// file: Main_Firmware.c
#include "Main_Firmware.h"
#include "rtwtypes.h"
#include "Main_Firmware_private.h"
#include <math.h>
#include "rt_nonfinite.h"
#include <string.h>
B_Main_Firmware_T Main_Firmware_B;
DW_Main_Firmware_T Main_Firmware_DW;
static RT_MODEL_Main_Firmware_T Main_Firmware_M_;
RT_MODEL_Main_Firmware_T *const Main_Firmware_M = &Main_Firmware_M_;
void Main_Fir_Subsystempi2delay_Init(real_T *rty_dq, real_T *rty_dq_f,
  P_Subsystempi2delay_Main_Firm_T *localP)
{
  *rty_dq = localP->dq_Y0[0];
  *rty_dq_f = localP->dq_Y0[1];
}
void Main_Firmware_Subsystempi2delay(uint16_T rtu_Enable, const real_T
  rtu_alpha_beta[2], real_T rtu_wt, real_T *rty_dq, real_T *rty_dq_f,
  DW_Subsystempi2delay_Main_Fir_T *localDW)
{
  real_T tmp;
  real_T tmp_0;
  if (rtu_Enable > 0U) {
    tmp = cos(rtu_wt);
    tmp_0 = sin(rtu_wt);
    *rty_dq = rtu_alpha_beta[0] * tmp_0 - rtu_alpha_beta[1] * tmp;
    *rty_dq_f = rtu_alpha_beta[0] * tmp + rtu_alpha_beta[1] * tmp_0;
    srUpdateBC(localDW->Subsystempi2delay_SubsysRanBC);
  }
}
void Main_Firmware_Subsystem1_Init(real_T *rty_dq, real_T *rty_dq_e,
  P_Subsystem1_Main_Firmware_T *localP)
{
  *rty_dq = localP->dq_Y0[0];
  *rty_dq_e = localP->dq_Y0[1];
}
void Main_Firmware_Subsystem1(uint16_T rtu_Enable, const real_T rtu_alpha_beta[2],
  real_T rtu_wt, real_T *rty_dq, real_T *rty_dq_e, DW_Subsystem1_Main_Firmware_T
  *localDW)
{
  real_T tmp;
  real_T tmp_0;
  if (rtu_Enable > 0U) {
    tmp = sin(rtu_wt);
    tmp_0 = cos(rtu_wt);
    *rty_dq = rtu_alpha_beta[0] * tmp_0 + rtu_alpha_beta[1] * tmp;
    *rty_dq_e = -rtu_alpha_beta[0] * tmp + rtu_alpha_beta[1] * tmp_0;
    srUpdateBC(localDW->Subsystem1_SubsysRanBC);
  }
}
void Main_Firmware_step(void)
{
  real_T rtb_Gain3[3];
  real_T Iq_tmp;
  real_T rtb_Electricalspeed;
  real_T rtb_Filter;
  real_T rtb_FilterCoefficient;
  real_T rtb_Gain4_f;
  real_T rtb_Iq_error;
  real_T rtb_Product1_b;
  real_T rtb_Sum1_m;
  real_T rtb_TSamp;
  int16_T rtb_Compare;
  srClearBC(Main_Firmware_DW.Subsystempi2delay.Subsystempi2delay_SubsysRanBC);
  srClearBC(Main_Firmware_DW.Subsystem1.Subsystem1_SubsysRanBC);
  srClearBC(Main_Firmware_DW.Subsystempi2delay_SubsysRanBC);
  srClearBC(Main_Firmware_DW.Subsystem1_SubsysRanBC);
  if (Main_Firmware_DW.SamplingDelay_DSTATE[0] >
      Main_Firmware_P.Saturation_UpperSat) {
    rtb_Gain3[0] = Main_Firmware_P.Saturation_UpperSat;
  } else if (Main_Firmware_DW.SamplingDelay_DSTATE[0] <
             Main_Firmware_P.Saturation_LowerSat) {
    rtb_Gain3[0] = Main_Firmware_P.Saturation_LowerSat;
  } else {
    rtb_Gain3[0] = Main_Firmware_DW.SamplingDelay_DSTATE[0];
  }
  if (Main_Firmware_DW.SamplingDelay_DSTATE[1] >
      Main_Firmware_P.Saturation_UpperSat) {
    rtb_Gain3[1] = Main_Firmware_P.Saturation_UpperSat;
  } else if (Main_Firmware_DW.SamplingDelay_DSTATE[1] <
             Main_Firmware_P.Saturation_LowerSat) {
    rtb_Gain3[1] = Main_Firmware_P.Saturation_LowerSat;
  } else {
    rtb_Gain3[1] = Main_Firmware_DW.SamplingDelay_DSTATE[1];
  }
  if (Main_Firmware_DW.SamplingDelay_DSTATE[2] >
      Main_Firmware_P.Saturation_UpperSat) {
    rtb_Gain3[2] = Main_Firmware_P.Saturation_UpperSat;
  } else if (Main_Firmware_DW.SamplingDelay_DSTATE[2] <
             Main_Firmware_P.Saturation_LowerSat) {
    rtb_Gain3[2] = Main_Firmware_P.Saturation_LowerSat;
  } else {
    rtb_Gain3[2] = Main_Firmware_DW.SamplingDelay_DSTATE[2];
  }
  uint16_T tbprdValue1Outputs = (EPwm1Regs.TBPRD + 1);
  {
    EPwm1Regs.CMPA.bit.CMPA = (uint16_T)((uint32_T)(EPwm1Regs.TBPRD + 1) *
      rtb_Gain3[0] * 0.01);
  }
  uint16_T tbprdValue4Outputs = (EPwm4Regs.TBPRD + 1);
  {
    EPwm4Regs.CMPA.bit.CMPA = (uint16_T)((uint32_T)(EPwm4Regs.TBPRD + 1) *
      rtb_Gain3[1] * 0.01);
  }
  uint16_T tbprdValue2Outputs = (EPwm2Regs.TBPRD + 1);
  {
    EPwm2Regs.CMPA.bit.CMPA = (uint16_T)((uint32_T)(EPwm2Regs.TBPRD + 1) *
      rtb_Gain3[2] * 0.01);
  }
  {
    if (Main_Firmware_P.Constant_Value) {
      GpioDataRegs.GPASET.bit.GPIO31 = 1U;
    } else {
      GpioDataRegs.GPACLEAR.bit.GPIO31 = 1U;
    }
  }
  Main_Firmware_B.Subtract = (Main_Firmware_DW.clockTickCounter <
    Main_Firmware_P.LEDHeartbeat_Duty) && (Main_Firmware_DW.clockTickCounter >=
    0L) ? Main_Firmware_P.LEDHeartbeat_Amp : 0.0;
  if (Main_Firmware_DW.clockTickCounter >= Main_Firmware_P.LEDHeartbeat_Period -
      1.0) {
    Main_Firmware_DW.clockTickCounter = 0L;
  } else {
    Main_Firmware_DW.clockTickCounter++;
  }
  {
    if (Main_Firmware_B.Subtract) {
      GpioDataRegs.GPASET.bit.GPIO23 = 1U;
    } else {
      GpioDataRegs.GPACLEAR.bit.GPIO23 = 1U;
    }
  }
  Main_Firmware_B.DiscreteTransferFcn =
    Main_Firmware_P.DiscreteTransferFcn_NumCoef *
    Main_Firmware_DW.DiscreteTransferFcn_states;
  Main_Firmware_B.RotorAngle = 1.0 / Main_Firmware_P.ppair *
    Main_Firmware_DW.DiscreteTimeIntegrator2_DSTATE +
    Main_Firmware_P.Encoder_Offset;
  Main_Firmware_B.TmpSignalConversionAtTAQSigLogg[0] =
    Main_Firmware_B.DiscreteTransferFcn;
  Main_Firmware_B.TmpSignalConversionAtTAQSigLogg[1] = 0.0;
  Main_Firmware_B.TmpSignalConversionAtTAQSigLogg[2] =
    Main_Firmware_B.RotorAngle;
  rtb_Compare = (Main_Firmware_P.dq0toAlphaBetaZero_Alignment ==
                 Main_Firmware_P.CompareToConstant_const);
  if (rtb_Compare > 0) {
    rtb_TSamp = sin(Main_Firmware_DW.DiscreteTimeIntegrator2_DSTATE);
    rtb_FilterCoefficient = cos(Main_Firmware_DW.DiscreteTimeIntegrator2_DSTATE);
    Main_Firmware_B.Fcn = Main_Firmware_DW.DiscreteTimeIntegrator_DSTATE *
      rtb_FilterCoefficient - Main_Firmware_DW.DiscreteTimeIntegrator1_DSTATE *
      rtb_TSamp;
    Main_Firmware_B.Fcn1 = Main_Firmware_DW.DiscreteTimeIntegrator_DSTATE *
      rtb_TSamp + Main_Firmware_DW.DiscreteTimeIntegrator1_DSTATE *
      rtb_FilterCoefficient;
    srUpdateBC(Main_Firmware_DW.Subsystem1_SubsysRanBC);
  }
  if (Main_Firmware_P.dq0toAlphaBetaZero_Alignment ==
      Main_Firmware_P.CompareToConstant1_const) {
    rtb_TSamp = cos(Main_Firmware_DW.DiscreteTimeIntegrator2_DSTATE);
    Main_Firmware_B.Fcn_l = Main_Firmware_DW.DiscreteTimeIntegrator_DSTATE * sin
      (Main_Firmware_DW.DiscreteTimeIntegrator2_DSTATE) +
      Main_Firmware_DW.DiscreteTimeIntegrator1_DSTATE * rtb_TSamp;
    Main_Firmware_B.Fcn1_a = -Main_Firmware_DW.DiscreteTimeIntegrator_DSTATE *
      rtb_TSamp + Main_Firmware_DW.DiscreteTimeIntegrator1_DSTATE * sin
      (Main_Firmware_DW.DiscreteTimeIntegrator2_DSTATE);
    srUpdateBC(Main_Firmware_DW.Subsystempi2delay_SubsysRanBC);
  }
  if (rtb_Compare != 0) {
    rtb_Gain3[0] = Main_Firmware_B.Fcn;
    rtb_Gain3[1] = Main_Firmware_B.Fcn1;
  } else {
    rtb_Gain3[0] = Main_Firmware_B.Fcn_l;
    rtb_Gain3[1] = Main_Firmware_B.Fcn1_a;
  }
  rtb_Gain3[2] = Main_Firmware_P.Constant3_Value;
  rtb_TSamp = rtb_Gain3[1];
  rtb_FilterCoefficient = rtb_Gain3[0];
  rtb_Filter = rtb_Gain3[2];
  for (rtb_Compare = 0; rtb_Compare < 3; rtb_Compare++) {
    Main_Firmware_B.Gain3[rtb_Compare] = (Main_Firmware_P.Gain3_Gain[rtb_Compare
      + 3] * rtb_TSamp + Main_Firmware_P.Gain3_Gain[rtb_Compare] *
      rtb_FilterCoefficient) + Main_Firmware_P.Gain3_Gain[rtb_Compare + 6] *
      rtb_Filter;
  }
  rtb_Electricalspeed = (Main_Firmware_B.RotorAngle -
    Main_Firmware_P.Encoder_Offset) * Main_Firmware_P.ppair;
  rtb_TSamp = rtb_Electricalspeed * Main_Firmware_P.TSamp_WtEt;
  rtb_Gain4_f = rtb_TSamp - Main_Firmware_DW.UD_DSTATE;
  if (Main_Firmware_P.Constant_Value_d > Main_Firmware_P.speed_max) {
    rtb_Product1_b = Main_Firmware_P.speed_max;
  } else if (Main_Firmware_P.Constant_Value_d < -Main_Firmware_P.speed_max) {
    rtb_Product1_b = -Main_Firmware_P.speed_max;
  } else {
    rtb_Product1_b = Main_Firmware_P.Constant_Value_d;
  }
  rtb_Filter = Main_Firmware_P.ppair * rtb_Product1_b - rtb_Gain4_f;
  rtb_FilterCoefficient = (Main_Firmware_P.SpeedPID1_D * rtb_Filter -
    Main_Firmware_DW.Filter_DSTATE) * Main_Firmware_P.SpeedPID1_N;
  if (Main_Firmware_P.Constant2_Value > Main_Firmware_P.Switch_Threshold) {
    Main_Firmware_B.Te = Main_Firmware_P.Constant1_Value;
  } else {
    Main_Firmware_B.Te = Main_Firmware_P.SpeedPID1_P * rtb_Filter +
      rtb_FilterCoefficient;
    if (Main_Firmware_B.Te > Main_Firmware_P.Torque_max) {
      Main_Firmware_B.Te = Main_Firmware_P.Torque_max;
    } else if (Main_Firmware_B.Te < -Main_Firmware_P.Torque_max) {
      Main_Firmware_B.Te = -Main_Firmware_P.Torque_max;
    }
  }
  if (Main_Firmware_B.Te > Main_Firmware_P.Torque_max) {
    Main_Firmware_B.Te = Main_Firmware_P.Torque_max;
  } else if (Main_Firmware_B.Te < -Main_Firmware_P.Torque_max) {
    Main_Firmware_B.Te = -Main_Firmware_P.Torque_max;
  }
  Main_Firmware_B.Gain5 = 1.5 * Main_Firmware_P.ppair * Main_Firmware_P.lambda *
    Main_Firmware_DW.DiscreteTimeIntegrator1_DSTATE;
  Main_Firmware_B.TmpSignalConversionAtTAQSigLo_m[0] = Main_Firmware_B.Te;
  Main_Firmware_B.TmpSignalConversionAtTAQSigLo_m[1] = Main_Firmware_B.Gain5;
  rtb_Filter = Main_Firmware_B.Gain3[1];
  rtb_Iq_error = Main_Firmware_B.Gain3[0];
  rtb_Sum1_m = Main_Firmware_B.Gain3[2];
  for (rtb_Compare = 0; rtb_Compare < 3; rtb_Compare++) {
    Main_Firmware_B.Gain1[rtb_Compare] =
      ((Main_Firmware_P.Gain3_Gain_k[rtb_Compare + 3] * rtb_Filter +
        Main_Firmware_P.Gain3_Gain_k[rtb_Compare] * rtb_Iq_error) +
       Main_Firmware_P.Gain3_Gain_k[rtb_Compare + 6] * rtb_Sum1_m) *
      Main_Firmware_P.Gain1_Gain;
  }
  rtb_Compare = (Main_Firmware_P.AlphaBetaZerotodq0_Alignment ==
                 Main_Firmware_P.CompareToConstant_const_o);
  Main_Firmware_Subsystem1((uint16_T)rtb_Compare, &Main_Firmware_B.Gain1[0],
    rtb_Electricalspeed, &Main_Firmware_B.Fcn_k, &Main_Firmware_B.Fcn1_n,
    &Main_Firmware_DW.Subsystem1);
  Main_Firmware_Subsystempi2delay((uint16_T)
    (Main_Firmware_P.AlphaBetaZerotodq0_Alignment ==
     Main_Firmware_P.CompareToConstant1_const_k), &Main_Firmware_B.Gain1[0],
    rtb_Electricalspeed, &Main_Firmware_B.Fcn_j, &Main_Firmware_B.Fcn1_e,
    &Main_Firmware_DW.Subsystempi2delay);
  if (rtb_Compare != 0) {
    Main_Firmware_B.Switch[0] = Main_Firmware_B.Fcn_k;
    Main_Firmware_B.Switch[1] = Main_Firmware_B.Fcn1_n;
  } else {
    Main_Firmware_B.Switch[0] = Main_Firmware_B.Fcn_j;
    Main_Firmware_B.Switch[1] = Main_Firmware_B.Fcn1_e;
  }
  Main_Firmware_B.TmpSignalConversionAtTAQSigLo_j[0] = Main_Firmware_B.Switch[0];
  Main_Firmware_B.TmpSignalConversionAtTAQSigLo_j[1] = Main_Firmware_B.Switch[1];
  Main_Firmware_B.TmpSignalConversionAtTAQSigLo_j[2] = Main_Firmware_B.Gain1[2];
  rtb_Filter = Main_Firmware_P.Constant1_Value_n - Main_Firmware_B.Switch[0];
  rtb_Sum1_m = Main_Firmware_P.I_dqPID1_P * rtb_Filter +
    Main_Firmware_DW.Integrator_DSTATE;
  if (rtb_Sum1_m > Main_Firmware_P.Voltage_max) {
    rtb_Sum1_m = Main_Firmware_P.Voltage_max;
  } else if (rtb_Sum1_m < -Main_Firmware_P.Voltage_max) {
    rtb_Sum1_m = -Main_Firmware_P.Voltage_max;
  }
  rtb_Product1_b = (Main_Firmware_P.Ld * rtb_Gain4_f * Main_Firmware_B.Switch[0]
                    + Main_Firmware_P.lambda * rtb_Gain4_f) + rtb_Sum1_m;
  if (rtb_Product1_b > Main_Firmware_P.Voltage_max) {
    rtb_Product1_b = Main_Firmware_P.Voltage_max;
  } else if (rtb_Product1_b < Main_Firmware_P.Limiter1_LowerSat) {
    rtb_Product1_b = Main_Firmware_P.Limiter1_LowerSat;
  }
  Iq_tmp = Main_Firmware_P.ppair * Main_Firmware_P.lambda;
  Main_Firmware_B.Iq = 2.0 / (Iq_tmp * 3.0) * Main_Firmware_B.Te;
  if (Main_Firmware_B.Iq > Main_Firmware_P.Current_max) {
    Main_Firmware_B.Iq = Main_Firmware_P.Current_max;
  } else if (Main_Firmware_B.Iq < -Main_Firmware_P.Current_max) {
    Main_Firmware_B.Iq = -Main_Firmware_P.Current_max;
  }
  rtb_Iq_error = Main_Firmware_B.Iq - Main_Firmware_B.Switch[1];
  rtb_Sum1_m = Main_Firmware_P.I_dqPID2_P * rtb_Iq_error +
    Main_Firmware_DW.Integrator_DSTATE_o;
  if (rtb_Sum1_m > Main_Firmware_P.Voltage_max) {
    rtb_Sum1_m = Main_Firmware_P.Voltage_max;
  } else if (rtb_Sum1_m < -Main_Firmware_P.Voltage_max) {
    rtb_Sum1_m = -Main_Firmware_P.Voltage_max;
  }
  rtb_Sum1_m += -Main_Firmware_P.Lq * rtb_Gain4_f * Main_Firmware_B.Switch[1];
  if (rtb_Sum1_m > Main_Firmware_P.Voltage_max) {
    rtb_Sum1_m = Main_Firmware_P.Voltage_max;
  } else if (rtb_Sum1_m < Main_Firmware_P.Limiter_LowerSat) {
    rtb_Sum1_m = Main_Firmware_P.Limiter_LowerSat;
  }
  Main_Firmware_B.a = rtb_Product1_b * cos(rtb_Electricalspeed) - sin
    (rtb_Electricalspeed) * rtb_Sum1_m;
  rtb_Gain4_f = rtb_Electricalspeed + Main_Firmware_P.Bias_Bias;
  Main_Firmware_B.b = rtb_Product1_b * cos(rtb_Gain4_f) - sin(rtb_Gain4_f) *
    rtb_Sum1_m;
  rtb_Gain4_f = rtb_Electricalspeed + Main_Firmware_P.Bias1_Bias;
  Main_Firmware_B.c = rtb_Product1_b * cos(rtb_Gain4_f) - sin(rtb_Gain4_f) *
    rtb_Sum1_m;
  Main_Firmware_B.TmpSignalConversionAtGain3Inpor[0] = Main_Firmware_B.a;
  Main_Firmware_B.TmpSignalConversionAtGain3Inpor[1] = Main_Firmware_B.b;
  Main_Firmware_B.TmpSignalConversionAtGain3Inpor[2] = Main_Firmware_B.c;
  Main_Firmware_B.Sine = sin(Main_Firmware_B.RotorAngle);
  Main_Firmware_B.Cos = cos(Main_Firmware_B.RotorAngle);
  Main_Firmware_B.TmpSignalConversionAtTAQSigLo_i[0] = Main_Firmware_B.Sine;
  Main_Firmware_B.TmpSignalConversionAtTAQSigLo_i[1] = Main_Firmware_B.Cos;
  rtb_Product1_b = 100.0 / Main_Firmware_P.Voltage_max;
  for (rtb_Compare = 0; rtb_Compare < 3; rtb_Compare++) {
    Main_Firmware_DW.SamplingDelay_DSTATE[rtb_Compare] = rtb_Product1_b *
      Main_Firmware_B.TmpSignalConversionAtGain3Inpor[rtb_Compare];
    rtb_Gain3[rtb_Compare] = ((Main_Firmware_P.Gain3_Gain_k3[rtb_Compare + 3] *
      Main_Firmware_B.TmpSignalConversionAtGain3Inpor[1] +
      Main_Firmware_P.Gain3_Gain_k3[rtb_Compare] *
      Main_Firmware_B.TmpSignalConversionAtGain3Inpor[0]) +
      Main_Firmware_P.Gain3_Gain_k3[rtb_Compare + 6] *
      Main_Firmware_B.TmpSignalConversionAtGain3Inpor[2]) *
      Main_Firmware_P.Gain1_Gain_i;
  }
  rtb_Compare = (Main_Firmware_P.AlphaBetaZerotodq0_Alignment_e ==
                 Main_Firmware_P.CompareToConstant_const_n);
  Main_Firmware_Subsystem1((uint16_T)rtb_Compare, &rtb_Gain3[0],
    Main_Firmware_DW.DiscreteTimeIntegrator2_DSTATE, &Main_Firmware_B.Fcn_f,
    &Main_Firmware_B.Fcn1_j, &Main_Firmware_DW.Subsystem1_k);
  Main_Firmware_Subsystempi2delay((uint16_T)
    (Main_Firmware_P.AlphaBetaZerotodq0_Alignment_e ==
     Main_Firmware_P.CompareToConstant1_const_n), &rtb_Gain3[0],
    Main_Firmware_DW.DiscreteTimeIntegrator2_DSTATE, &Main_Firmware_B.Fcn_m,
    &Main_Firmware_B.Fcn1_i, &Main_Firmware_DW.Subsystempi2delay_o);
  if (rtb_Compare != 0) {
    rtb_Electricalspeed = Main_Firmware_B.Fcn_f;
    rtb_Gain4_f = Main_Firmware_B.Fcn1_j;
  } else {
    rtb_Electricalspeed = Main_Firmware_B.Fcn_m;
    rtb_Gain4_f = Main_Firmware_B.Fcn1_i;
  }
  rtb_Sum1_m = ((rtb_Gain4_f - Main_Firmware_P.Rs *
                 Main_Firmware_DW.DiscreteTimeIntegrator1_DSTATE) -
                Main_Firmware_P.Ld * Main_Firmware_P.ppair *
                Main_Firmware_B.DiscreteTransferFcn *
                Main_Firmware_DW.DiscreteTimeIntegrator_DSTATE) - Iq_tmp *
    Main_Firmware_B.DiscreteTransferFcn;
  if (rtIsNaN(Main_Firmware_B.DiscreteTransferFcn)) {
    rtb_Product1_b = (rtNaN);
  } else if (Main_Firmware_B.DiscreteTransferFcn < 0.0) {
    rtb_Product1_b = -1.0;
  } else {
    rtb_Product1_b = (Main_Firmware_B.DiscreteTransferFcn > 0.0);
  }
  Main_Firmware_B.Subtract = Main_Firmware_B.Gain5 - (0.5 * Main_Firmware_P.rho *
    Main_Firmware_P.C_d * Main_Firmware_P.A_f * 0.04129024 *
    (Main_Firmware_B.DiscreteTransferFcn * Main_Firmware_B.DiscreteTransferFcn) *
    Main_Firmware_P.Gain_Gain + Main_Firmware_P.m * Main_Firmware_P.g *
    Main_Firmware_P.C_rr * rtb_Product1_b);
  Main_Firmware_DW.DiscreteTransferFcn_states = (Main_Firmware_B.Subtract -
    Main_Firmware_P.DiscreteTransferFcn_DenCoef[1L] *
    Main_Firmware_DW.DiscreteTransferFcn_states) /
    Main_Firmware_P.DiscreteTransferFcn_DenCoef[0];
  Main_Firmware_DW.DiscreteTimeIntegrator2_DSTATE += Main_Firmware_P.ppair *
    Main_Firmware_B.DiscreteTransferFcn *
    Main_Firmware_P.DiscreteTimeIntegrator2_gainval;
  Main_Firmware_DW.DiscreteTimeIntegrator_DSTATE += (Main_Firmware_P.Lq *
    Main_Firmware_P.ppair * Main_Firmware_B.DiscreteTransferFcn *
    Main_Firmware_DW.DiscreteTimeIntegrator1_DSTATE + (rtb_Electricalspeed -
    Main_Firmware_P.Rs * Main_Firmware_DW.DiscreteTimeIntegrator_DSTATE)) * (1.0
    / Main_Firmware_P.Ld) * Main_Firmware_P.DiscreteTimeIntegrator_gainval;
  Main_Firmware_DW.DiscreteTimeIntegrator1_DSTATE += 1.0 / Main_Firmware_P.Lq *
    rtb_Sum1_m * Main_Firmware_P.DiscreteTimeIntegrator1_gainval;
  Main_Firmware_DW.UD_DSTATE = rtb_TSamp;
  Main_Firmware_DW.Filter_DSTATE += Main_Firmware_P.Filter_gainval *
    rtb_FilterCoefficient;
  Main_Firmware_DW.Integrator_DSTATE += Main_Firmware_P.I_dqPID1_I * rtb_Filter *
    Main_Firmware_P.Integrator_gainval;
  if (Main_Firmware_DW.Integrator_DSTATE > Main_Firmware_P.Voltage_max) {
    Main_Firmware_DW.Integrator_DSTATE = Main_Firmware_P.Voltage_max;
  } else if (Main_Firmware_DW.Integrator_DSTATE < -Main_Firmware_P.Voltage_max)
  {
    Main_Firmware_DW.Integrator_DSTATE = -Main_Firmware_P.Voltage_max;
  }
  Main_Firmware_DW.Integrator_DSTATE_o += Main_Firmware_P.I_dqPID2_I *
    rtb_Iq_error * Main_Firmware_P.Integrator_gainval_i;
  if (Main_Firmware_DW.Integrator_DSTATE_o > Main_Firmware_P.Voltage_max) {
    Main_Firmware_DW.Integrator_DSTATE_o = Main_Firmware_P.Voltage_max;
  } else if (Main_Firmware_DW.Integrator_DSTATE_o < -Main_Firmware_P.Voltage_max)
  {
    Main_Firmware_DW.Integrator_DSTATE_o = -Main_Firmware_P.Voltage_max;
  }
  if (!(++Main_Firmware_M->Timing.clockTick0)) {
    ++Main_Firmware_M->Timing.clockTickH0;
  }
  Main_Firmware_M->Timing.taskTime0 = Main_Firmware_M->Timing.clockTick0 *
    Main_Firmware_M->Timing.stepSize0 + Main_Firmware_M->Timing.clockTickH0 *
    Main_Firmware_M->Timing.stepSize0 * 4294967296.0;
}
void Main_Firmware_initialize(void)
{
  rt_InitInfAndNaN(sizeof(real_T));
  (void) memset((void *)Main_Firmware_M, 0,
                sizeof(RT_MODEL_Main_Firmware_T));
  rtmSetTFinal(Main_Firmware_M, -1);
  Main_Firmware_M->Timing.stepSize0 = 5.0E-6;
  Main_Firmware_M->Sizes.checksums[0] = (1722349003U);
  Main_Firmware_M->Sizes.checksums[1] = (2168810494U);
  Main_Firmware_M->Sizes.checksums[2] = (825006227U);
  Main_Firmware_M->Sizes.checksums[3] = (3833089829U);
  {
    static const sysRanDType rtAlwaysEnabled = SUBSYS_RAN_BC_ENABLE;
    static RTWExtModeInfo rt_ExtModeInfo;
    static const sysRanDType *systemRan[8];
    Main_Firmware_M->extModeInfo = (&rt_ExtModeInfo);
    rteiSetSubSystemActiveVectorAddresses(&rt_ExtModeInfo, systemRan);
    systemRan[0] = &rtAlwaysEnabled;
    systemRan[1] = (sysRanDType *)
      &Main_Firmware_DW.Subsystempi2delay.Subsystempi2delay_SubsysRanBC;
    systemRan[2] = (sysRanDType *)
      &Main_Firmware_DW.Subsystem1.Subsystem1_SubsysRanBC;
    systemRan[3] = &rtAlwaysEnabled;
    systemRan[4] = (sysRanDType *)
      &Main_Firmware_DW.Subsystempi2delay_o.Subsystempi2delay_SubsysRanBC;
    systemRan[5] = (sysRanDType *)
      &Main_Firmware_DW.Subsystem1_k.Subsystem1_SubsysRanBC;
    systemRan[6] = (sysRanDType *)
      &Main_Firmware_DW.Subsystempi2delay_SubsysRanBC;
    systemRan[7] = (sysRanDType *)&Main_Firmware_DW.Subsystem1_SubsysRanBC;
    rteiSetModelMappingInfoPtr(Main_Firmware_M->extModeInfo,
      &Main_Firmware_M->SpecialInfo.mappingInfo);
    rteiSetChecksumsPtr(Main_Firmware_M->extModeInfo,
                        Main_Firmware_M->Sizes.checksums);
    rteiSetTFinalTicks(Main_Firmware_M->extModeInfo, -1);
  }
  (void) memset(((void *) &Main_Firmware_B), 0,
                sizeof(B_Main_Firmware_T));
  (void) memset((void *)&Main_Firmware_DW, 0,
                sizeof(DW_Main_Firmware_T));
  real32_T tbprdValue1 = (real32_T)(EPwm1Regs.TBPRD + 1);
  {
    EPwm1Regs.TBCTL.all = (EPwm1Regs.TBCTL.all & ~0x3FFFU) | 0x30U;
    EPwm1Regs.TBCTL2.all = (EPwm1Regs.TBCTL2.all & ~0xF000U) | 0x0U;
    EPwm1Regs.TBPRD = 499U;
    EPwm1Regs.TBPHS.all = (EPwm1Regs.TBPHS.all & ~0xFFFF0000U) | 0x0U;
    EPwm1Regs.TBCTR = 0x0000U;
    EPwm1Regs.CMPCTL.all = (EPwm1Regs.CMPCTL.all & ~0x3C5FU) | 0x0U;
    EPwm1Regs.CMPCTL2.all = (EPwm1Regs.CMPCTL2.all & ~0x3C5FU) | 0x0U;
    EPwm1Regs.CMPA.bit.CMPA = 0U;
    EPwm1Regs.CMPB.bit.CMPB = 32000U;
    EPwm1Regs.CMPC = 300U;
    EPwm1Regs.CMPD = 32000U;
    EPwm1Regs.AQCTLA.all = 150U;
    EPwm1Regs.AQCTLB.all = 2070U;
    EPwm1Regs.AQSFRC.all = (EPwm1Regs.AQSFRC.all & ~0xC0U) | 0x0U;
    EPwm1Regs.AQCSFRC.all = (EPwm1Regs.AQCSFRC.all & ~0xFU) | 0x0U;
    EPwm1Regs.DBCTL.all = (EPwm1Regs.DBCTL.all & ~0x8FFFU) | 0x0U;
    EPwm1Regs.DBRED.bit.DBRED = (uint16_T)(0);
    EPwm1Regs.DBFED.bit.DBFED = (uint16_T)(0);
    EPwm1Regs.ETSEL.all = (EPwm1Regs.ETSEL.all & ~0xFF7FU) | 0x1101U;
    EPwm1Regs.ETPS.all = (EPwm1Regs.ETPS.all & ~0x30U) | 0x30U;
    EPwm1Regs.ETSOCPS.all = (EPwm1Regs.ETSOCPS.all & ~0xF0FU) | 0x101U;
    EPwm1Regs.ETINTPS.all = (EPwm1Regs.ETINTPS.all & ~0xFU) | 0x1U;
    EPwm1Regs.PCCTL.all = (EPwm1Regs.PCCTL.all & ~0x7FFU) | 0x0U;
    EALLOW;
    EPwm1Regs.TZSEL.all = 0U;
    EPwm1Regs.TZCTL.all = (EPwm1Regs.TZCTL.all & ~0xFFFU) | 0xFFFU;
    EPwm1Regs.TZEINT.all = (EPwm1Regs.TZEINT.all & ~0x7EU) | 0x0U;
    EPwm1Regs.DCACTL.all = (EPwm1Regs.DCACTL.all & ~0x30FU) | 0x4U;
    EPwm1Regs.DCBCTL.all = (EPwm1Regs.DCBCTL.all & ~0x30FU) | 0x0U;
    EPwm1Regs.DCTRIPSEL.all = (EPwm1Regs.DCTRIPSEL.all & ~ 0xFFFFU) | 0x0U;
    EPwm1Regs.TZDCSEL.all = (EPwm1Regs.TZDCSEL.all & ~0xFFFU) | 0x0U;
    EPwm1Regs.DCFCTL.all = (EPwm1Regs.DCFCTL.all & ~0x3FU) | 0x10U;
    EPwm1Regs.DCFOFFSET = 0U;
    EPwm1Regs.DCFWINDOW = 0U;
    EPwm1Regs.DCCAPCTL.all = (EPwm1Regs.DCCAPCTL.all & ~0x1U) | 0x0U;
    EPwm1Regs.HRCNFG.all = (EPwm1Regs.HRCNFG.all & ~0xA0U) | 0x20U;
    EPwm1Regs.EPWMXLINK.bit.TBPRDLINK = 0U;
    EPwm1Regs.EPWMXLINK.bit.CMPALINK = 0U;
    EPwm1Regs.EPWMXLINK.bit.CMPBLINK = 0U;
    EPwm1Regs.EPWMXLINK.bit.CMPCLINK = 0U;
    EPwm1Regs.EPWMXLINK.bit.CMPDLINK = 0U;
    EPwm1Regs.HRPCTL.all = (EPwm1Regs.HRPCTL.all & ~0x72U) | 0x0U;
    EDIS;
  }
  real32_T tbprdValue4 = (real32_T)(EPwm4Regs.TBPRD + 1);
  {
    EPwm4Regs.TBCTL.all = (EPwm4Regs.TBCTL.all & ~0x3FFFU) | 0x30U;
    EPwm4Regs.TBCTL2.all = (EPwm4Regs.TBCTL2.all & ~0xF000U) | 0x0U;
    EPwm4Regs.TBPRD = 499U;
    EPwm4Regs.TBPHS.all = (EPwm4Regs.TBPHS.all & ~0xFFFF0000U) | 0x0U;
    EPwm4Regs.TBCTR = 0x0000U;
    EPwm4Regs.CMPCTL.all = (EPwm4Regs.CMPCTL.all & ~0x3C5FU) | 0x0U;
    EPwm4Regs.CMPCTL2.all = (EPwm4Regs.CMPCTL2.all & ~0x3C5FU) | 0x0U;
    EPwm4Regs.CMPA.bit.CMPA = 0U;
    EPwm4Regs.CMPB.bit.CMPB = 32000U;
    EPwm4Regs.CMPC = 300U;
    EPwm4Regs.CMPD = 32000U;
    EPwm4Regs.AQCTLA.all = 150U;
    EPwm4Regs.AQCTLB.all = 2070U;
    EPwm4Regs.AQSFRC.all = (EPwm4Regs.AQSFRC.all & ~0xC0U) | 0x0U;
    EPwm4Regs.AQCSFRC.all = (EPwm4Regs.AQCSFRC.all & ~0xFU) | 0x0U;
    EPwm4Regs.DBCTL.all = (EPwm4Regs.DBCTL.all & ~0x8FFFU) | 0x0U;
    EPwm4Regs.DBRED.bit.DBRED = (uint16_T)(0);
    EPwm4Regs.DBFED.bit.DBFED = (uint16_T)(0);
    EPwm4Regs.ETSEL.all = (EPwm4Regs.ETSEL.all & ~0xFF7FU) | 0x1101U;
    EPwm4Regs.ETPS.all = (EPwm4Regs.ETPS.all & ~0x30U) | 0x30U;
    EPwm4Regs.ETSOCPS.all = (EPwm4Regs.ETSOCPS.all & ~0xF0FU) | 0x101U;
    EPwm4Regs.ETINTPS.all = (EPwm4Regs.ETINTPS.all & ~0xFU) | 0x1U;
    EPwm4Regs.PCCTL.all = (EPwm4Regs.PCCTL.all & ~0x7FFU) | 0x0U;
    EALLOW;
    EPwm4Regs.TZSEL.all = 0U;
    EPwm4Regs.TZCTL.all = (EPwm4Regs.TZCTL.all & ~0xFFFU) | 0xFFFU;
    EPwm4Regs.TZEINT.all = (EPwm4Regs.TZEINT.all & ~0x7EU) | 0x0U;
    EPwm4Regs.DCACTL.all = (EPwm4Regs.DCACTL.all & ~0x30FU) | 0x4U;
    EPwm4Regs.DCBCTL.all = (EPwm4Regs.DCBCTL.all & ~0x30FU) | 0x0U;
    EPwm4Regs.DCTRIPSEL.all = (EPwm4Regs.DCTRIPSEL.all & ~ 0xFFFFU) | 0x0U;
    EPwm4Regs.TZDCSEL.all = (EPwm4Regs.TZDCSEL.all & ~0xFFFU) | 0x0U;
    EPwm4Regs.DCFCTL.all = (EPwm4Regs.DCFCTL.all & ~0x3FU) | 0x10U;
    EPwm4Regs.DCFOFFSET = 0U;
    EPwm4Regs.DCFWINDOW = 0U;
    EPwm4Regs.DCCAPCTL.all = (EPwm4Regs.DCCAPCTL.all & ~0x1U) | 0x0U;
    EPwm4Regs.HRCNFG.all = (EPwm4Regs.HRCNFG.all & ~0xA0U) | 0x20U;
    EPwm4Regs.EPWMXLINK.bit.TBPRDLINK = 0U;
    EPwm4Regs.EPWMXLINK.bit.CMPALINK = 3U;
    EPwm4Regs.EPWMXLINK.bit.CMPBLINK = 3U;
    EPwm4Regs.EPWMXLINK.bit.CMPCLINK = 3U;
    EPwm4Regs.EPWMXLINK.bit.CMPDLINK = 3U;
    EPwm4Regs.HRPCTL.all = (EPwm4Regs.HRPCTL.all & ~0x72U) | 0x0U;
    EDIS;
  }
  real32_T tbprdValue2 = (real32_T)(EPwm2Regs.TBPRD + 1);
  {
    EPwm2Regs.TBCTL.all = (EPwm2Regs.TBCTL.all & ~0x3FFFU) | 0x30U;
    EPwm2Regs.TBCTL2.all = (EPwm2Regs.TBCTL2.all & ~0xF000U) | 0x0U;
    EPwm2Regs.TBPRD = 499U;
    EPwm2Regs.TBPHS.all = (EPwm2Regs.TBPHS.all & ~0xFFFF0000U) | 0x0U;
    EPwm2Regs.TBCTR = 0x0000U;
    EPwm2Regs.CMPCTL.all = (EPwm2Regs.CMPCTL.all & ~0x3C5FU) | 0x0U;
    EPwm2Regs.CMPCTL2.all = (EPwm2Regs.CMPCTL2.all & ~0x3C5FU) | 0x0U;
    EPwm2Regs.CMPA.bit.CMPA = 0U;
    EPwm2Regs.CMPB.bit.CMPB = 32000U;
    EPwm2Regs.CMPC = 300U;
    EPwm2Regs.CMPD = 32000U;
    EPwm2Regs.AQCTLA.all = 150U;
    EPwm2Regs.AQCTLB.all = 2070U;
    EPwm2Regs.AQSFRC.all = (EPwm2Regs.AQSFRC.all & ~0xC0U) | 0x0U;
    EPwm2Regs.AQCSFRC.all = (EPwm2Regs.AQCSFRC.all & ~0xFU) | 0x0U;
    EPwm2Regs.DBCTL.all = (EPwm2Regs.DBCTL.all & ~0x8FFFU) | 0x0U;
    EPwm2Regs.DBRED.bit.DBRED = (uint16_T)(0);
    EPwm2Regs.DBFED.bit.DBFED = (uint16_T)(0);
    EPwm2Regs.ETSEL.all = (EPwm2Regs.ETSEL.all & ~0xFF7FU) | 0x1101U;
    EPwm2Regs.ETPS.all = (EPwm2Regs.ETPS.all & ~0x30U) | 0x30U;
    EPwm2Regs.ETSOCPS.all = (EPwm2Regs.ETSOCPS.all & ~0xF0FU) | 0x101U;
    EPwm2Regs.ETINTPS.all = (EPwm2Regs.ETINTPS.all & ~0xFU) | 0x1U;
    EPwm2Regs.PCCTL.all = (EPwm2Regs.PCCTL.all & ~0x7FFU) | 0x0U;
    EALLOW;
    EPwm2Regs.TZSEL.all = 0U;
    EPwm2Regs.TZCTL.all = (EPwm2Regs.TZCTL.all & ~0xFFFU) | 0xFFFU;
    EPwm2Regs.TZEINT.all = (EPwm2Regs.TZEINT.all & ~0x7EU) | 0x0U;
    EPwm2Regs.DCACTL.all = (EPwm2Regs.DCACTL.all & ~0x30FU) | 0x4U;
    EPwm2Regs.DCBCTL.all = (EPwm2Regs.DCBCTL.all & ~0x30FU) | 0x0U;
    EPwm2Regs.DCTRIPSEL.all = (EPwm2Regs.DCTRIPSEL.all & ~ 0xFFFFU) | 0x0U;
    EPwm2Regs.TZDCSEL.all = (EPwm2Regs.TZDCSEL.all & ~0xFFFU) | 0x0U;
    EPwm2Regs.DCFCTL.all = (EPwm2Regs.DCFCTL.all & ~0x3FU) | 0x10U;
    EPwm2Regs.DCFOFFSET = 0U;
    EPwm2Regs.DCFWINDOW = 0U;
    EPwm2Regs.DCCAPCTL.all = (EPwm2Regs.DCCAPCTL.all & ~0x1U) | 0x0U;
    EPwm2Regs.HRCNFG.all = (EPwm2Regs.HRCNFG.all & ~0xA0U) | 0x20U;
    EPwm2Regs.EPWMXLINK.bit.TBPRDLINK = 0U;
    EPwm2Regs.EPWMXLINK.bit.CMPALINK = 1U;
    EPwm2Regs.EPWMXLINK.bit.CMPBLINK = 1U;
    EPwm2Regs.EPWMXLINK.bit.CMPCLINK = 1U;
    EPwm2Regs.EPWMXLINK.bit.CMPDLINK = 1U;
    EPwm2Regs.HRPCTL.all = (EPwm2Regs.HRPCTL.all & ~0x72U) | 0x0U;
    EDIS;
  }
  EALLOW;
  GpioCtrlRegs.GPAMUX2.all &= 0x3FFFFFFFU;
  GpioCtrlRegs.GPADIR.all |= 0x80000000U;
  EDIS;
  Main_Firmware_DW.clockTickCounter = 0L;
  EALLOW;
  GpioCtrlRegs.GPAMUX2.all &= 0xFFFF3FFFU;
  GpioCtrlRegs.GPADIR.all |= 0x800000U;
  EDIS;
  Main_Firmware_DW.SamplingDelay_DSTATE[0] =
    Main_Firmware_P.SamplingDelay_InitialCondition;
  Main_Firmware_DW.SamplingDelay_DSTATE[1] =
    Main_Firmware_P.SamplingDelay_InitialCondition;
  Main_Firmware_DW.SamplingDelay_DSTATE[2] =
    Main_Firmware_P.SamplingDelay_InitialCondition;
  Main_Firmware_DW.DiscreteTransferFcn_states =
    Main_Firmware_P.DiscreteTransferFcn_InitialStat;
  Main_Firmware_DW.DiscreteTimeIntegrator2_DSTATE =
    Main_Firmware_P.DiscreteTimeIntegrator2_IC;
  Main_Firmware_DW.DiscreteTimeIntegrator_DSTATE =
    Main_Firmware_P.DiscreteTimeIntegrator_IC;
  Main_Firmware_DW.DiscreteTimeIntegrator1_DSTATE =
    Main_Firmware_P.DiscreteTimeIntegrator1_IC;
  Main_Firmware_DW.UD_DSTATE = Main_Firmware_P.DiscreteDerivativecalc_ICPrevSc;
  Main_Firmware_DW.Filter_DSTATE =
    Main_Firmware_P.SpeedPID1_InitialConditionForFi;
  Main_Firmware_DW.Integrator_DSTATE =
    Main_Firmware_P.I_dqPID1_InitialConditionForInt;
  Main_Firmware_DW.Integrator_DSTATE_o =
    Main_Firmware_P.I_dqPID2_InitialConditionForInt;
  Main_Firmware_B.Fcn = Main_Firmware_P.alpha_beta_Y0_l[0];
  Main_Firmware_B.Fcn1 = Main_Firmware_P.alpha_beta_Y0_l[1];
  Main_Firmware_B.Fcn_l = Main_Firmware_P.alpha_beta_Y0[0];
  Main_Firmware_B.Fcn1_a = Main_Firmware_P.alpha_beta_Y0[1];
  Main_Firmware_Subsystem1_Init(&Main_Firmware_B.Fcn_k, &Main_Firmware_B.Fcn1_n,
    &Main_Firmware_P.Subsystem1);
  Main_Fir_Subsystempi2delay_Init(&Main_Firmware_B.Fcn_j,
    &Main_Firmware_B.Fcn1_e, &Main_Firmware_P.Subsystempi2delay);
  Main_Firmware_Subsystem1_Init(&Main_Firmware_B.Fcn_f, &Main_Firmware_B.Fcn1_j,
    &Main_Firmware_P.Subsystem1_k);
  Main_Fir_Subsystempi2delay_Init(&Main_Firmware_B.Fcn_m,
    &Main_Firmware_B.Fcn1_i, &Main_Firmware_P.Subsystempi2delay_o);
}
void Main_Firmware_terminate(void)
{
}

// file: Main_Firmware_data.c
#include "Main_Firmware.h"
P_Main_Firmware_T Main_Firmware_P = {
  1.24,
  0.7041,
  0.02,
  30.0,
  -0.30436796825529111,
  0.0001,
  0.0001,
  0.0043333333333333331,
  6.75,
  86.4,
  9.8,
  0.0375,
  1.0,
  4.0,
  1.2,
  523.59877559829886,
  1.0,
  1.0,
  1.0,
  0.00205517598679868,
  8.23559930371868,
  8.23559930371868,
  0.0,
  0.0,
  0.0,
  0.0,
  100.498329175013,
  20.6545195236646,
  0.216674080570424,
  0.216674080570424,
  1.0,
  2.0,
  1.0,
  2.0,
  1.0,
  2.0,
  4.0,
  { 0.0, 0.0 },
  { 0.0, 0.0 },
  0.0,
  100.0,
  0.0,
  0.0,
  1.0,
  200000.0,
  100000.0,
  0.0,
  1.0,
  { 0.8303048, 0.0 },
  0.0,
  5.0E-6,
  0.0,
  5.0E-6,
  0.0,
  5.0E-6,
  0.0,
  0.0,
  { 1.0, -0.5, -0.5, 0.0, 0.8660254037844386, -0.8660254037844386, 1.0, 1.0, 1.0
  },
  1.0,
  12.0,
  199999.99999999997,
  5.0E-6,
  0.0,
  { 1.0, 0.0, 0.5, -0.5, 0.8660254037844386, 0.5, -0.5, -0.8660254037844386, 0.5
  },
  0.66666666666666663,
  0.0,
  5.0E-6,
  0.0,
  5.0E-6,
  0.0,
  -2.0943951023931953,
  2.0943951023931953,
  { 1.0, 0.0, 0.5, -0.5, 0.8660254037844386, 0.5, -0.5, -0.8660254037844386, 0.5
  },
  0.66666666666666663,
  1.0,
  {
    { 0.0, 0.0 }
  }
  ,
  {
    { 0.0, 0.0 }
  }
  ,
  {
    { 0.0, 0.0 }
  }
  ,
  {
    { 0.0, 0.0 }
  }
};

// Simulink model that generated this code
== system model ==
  ePWM#1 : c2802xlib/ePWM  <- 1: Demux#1
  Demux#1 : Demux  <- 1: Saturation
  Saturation : Saturate  UpperLimit=100  LowerLimit=0  <- 1: SamplingDelay
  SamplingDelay : Delay  DelayLength=1  <- 1: Gain5
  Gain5 : Gain  Gain=100/Voltage_max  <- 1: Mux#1
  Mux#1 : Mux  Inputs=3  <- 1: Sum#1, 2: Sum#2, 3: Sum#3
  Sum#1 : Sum  Inputs=+-  <- 1: Product#1, 2: Product1
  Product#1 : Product  <- 1: Limiter1, 2: Trigonometry#1
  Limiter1 : Saturate  UpperLimit=Voltage_max  LowerLimit=0  <- 1: Sum1
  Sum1 : Sum  Inputs=++  <- 1: I_dqPID1, 2: Sum#4
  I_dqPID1 : slpidlib/PID Controller  Controller=PI  Form=Parallel  TimeDomain=Discrete-time  IntegratorMethod=Forward Euler  P=0.216674080570424  I=8.23559930371868  D=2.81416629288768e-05  N=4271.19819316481  InitialConditionForIntegrator=0  ExternalReset=none  LimitOutput=on  UpperSaturationLimit=Voltage_max  LowerSaturationLimit=-Voltage_max  <- 1: Sum#5
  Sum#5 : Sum  Inputs=+-  <- 1: Constant1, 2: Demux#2
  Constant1 : Constant  Value=0
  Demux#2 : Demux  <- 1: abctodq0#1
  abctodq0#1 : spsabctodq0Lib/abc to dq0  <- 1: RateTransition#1, 2: Gain#1
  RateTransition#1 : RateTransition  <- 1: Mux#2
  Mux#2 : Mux  Inputs=3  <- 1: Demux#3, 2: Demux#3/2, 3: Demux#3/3
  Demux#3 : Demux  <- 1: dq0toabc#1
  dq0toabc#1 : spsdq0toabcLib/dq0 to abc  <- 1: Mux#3, 2: DiscreteTimeIntegrator2
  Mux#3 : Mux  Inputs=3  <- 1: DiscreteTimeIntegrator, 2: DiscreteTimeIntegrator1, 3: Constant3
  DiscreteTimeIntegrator : DiscreteIntegrator  <- 1: Gain
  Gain : Gain  Gain=1/Ld  <- 1: Sum#6
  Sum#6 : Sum  Inputs=+-+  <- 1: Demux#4, 2: Gain1, 3: Product#2
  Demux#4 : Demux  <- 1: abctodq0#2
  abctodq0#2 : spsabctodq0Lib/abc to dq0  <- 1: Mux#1, 2: DiscreteTimeIntegrator2
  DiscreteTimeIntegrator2 : DiscreteIntegrator  <- 1: Gain#2
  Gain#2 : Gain  Gain=ppair  <- 1: DiscreteTransferFcn
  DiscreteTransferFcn : DiscreteTransferFcn  Denominator=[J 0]  <- 1: Subtract
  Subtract : Sum  Inputs=+-  <- 1: Gain#3, 2: Sum#7
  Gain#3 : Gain  Gain=3/2*ppair*lambda  <- 1: DiscreteTimeIntegrator1
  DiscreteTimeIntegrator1 : DiscreteIntegrator  <- 1: Gain#4
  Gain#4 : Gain  Gain=1/Lq  <- 1: Sum#8
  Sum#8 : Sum  Inputs=+---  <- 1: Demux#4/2, 2: Gain3, 3: Product#3, 4: Gain4
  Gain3 : Gain  Gain=Rs  <- 1: DiscreteTimeIntegrator1
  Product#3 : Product  Inputs=3  <- 1: Constant#1, 2: DiscreteTransferFcn, 3: DiscreteTimeIntegrator
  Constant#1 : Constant  Value=Ld*ppair
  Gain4 : Gain  Gain=ppair*lambda  <- 1: DiscreteTransferFcn
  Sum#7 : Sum  Inputs=++  <- 1: Gain#5, 2: Product#4
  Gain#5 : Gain  Gain=1/k^2  <- 1: Product#5
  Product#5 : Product  <- 1: Constant#2, 2: Math#1
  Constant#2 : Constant  Value=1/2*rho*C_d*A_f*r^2
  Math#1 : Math  Operator=square  <- 1: DiscreteTransferFcn
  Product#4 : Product  <- 1: Constant2, 2: Signum#1
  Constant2 : Constant  Value=m*g*C_rr
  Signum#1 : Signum  <- 1: DiscreteTransferFcn
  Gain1 : Gain  Gain=Rs  <- 1: DiscreteTimeIntegrator
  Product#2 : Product  Inputs=3  <- 1: Constant, 2: DiscreteTransferFcn, 3: DiscreteTimeIntegrator1
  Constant : Constant  Value=Lq*ppair
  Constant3 : Constant  Value=0
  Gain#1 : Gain  Gain=ppair  <- 1: Sum#9
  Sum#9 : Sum  Inputs=+-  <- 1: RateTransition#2, 2: Constant#3
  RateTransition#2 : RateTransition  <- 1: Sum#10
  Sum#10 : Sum  Inputs=++  <- 1: Gain#6, 2: Constant#4
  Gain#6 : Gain  Gain=1/ppair  <- 1: DiscreteTimeIntegrator2
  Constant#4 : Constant  Value=Encoder_Offset
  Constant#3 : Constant  Value=Encoder_Offset
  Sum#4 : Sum  <- 1: Product#6, 2: Gain#7
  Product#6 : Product  <- 1: Gain#8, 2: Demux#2
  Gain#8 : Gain  Gain=Ld  <- 1: DiscreteDerivativecalc
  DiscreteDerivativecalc : simulink/Discrete/Discrete Derivative  gainval=1.0  <- 1: Gain#1
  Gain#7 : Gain  Gain=lambda  <- 1: DiscreteDerivativecalc
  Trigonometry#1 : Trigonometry  Operator=cos  <- 1: Gain#1
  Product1 : Product  <- 1: Trigonometry#2, 2: Limiter
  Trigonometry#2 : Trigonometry  <- 1: Gain#1
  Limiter : Saturate  UpperLimit=Voltage_max  LowerLimit=0  <- 1: Sum#11
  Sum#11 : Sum  Inputs=++  <- 1: I_dqPID2, 2: Product#7
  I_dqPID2 : slpidlib/PID Controller  Controller=PI  Form=Parallel  TimeDomain=Discrete-time  IntegratorMethod=Forward Euler  P=0.216674080570424  I=8.23559930371868  D=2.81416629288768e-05  N=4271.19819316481  InitialConditionForIntegrator=0  ExternalReset=none  LimitOutput=on  UpperSaturationLimit=Voltage_max  LowerSaturationLimit=-Voltage_max  <- 1: Sum#12
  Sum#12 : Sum  Inputs=+-  <- 1: Saturate#1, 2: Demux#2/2
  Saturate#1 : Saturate  UpperLimit=Current_max  LowerLimit=-Current_max  <- 1: Gain#9
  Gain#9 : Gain  Gain=2/(ppair*lambda*3)  <- 1: Saturate#2
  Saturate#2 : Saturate  UpperLimit=Torque_max  LowerLimit=-Torque_max  <- 1: Switch
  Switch : Switch  Criteria=u2 > Threshold  <- 1: Constant#5, 2: Constant#6, 3: SpeedPID1
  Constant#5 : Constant  Value=4
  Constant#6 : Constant
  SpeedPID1 : slpidlib/PID Controller  Controller=PD  Form=Parallel  TimeDomain=Discrete-time  IntegratorMethod=Forward Euler  P=20.6545195236646  I=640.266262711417  D=0.00205517598679868  N=100.498329175013  InitialConditionForIntegrator=0  ExternalReset=none  LimitOutput=on  UpperSaturationLimit=Torque_max  LowerSaturationLimit=-Torque_max  <- 1: Sum#13
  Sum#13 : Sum  Inputs=+-  <- 1: Gain#10, 2: DiscreteDerivativecalc
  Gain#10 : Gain  Gain=ppair  <- 1: Saturate#3
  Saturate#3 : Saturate  UpperLimit=speed_max  LowerLimit=-speed_max  <- 1: Constant#7
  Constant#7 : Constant  Value=12
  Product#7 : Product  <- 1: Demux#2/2, 2: Gain#11
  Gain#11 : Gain  Gain=-Lq  <- 1: DiscreteDerivativecalc
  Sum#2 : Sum  Inputs=+-  <- 1: Product#8, 2: Product#9
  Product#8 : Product  <- 1: Limiter1, 2: Trigonometry#3
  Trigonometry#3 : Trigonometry  Operator=cos  <- 1: Bias
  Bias : Bias  Bias=-2*pi/3  <- 1: Gain#1
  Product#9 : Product  <- 1: Trigonometry#4, 2: Limiter
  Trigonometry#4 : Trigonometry  <- 1: Bias
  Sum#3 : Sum  Inputs=+-  <- 1: Product#10, 2: Product#11
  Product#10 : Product  <- 1: Limiter1, 2: Trigonometry#5
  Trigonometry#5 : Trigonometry  Operator=cos  <- 1: Bias1
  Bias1 : Bias  Bias=2*pi/3  <- 1: Gain#1
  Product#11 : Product  <- 1: Trigonometry#6, 2: Limiter
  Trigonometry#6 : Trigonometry  <- 1: Bias1
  ePWM#2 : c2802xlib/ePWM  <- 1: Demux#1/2
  ePWM#3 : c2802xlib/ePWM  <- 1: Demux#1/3
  DigitalOutput#1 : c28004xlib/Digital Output  <- 1: Constant#8
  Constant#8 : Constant  Value=0
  DigitalOutput#2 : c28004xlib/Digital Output  <- 1: LEDHeartbeat
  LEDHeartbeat : DiscretePulseGenerator  Period=1  PulseWidth=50
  Mux#4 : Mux  Inputs=3  <- 1: DiscreteTransferFcn, 3: Sum#10
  Mux#5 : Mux  Inputs=2  <- 1: Saturate#2, 2: Gain#3
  Mux#6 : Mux  Inputs=2  <- 1: Trigonometry#7, 2: Trigonometry#8
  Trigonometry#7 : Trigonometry  <- 1: Sum#10
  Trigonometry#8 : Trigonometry  Operator=cos  <- 1: Sum#10
